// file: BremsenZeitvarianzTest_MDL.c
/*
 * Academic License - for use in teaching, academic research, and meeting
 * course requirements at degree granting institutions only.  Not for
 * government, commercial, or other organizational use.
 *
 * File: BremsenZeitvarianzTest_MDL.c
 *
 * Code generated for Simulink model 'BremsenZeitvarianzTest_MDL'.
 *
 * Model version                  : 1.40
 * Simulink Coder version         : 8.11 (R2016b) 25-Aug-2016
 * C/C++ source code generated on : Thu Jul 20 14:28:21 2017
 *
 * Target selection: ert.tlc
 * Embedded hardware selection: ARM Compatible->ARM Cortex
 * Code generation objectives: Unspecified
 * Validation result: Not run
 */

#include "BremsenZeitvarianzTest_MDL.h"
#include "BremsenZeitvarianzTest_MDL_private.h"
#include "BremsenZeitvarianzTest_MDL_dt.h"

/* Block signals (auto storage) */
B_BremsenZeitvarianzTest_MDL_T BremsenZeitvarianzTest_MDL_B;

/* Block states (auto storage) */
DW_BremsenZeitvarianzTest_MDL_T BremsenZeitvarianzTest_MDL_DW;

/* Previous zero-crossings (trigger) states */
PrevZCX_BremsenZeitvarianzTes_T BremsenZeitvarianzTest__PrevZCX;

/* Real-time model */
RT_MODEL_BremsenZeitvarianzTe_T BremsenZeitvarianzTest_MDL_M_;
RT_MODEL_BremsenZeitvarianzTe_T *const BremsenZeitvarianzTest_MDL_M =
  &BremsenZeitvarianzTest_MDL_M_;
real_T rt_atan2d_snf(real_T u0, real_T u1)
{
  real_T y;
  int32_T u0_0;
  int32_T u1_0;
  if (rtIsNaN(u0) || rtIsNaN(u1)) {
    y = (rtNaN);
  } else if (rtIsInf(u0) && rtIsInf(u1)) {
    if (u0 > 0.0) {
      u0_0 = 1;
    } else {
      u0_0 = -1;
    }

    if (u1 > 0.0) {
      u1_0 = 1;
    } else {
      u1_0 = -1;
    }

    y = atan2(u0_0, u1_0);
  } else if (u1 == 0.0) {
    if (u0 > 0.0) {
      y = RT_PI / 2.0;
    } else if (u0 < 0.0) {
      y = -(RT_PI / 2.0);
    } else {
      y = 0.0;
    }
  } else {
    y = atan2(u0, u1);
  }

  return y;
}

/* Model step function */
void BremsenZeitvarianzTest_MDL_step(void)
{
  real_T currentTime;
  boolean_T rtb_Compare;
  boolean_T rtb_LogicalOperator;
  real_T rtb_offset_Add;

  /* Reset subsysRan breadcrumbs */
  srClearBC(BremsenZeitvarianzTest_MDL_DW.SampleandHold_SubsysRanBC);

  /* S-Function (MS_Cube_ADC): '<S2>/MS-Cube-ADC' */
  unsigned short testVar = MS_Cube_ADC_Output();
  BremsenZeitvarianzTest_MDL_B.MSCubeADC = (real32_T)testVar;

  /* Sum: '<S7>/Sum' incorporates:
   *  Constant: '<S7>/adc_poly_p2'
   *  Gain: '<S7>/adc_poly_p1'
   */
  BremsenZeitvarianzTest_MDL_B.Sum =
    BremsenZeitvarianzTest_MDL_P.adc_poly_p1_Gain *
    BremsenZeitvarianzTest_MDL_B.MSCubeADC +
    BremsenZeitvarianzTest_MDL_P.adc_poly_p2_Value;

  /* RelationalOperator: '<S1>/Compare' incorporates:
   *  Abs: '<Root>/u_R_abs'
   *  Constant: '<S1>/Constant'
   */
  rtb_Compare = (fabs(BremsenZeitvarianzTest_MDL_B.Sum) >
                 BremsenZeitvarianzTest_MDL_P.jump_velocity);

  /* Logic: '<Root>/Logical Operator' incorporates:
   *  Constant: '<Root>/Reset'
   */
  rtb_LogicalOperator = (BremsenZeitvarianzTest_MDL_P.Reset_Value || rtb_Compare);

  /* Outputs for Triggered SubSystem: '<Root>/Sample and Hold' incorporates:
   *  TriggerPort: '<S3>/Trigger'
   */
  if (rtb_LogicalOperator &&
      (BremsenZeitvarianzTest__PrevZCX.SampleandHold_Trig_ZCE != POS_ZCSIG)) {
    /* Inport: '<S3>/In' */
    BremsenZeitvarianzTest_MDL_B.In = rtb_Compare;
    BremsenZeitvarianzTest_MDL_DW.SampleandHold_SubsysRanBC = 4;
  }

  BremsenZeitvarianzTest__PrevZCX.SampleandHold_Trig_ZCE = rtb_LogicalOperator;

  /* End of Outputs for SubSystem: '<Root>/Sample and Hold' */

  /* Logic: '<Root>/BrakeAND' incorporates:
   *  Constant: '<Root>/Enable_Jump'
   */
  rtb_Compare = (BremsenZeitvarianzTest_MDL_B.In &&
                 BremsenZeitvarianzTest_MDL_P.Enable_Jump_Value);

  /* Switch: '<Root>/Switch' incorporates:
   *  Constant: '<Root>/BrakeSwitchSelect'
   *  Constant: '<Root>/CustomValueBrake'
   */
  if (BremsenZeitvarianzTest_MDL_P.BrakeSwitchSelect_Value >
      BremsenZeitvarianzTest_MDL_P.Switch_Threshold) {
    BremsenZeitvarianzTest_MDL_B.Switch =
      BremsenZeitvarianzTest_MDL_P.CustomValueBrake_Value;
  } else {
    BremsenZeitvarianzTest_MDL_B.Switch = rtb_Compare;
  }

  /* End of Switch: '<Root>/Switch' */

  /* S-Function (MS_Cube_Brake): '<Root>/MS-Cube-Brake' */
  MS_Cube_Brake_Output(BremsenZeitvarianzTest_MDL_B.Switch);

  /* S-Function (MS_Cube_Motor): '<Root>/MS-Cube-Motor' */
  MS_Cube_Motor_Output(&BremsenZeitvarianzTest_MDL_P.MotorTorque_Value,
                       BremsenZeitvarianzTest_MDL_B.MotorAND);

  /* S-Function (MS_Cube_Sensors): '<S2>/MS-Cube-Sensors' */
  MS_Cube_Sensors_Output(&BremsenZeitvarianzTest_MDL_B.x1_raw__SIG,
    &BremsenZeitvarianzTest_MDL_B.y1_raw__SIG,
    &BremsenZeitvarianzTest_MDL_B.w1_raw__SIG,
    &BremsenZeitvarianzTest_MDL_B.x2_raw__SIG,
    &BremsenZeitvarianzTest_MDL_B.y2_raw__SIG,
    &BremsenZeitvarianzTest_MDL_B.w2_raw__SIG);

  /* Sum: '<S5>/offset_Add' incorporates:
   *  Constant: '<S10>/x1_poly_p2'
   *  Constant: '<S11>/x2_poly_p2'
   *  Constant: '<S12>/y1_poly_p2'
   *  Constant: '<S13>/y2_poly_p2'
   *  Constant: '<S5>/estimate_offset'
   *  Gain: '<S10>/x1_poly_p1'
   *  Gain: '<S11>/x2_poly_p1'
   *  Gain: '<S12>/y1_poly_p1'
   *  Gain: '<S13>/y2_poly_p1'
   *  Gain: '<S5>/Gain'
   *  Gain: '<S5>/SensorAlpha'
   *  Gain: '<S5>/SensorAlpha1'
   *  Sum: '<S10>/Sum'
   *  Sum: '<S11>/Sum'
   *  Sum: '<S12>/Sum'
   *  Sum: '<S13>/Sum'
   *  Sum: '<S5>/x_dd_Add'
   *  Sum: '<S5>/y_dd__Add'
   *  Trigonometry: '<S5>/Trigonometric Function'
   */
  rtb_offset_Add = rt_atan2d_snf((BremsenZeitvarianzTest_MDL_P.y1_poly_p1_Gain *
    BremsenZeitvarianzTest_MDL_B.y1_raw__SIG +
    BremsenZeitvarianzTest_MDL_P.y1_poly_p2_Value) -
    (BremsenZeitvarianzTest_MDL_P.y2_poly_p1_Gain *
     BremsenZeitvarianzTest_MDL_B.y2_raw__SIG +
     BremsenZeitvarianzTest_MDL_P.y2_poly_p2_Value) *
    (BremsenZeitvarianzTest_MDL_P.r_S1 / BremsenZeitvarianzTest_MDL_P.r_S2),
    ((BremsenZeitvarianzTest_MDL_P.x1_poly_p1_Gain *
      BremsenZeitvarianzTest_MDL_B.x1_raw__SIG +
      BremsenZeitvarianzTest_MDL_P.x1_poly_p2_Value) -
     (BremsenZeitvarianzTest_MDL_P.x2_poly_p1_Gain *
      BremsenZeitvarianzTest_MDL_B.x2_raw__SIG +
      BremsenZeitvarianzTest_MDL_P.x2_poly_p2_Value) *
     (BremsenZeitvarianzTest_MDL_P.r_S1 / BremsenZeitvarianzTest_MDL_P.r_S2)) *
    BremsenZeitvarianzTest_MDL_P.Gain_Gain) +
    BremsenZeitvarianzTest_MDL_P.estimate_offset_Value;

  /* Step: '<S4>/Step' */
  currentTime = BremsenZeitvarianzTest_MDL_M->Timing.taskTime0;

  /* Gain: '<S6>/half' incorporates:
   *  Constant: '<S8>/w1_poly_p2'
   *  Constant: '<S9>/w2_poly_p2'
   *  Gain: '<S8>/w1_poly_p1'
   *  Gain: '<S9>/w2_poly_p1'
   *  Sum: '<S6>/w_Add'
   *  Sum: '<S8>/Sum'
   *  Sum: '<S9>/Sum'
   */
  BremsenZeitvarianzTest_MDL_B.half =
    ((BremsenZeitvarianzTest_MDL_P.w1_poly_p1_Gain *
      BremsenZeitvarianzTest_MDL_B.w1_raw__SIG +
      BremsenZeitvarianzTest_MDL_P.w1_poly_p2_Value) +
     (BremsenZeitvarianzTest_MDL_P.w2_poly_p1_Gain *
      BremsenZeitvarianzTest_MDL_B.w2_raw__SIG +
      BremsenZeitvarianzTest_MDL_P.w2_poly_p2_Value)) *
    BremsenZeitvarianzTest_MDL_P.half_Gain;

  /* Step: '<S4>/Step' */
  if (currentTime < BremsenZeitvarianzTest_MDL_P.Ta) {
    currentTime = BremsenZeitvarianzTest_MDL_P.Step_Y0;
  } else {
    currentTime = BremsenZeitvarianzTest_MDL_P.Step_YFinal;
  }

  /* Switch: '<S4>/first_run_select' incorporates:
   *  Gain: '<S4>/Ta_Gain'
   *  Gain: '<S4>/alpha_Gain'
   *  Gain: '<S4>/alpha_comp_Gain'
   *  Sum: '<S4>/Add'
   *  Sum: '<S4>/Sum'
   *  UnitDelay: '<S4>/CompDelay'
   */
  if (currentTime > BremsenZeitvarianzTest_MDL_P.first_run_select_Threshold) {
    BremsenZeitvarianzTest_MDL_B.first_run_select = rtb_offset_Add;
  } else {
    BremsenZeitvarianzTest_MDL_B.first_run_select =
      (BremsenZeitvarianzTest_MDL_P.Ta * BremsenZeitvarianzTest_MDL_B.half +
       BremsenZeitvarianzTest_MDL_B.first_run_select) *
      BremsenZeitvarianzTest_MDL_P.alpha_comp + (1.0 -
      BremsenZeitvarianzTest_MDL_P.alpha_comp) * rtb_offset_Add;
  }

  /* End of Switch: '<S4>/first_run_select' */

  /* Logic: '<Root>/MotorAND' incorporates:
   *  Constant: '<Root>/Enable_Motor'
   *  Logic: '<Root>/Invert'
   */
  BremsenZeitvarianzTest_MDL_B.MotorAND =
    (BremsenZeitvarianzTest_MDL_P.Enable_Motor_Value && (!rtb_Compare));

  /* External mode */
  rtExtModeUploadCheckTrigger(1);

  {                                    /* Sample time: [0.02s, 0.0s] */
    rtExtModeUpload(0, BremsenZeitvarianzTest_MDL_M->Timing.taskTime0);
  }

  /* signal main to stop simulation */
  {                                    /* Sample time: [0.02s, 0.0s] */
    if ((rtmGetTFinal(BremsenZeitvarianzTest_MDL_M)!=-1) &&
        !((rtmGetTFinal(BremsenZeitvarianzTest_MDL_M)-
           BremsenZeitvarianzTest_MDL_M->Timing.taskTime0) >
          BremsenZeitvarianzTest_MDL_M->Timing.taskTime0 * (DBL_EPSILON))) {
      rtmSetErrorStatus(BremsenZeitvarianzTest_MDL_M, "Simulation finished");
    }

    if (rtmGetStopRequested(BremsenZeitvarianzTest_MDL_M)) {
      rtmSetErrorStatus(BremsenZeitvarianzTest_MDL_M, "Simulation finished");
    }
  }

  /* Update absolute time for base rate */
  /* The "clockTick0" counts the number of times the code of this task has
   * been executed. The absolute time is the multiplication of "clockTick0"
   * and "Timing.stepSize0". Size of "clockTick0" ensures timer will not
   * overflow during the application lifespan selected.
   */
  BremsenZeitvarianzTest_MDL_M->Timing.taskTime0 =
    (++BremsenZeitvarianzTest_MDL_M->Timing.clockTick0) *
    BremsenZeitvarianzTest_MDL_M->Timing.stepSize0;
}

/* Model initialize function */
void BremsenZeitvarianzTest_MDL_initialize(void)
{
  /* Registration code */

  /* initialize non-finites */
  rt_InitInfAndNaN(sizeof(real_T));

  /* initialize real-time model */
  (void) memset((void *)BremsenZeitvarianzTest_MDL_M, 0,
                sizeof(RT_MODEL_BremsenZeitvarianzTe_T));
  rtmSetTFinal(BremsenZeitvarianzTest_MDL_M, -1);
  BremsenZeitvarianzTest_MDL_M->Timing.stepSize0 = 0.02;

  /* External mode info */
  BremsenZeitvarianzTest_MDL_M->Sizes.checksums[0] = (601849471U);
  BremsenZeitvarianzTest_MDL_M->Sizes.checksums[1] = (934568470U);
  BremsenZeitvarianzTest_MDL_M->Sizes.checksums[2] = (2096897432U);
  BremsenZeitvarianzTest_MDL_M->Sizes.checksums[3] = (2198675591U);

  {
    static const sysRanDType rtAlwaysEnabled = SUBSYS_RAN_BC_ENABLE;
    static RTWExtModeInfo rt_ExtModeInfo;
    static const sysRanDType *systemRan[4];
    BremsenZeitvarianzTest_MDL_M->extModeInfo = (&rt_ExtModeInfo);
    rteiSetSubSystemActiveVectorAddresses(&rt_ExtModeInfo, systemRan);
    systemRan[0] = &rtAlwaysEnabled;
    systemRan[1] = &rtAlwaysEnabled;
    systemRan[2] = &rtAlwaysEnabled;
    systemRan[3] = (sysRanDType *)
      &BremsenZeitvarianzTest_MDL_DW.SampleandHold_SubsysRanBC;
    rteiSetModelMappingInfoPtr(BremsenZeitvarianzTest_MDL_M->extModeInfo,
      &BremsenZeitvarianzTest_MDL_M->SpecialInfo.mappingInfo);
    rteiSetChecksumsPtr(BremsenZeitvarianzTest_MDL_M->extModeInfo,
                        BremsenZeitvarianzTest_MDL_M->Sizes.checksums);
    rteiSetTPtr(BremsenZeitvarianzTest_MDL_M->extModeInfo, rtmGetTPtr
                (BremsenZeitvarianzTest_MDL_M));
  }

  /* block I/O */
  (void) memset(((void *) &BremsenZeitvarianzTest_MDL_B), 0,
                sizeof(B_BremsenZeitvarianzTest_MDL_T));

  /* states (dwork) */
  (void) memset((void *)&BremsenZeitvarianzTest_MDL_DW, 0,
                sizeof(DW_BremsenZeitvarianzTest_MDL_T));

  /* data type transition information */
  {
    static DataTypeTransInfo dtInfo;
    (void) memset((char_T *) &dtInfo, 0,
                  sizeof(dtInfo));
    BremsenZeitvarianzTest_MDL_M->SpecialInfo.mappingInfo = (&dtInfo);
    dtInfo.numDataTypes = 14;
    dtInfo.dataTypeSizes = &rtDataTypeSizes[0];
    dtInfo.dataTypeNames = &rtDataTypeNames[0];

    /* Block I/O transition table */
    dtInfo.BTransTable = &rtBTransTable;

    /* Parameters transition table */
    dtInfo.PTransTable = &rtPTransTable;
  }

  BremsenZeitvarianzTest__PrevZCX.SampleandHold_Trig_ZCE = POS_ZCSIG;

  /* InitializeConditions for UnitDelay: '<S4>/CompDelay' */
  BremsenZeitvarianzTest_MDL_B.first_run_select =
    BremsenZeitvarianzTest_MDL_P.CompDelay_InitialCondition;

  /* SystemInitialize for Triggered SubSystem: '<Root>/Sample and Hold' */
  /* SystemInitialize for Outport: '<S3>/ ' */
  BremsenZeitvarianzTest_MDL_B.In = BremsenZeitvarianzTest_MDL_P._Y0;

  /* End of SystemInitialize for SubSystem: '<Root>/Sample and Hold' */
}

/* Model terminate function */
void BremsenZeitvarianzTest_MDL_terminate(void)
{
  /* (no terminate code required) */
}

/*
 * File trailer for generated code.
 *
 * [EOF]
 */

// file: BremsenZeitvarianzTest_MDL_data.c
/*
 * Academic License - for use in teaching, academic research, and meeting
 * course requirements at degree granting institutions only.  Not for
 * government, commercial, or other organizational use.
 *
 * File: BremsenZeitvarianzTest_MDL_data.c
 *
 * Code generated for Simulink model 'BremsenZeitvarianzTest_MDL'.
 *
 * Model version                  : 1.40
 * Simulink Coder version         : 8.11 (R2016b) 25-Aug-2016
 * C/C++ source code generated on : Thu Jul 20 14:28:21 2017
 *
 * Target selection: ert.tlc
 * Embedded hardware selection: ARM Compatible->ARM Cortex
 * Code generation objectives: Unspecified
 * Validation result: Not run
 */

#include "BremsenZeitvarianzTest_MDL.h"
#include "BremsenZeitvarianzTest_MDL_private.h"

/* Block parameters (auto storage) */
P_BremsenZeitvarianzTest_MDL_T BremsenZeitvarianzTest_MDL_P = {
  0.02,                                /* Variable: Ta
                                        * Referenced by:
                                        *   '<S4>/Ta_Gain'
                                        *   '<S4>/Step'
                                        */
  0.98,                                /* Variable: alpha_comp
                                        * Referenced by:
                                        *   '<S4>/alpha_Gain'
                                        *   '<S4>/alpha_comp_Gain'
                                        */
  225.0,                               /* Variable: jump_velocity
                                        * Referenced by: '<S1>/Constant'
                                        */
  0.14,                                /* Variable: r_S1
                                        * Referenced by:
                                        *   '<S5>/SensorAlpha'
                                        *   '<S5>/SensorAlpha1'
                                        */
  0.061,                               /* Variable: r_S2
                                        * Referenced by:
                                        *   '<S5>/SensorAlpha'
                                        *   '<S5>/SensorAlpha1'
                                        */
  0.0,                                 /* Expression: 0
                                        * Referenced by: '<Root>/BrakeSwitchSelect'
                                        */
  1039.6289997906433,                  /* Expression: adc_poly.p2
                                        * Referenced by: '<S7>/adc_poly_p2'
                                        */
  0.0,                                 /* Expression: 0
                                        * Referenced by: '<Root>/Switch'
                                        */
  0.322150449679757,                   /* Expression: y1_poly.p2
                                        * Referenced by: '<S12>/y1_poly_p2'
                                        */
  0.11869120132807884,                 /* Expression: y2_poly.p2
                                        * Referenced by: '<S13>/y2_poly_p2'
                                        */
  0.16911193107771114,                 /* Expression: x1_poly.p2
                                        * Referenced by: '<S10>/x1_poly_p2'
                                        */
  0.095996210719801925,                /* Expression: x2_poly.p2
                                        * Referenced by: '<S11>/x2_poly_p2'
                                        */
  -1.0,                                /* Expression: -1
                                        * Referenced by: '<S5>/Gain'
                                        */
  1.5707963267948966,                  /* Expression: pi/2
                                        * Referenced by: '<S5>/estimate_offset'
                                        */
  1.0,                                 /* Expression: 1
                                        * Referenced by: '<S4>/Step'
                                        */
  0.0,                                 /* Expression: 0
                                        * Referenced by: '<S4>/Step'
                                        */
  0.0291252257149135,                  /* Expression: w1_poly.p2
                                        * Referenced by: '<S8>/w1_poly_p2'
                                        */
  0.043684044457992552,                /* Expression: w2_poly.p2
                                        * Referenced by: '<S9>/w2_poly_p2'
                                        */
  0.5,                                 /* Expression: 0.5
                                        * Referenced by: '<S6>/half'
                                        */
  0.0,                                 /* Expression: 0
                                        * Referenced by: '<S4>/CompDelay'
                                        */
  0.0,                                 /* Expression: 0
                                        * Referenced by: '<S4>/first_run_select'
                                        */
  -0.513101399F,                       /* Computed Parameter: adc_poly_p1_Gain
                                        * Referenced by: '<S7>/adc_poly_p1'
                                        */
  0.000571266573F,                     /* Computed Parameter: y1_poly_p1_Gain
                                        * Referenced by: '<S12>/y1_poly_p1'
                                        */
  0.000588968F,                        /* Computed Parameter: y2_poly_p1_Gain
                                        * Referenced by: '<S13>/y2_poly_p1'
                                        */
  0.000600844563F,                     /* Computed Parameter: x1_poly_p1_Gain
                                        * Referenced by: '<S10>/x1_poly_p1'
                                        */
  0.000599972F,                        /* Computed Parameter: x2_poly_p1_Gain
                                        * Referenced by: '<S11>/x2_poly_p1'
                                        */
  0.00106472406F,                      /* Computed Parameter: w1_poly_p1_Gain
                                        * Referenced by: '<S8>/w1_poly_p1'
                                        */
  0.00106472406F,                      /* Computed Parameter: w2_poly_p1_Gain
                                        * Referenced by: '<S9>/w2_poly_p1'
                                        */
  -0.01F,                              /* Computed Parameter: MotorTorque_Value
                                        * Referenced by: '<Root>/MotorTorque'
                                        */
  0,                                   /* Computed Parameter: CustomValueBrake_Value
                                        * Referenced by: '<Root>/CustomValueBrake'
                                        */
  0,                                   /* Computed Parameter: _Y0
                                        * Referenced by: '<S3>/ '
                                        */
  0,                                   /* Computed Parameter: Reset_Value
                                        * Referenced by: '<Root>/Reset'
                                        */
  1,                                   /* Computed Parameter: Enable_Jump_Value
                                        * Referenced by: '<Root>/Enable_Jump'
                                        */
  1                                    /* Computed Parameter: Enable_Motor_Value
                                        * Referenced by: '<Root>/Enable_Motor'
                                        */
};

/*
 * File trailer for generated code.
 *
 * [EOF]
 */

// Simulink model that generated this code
simulink model "BremsenZeitvarianzTest_MDL"  (R2016b)
settings: Solver=FixedStepAuto  StartTime=0.0  StopTime=inf  FixedStep=Ta  RelTol=1e-3
values from neighbouring files (symbols this model uses):
  alpha_comp = 0.98    [ModelSetup.m]
  jump_velocity = 200    [ModelSetup.m]
  r_S1 = 0.14    [ModelSetup.m]
  r_S2 = 0.061    [ModelSetup.m]
  Ta = 0.02    [ModelSetup.m]
undefined symbols (not defined in the file or in its folder): adc_poly, w1_poly, w2_poly, x1_poly, x2_poly, y1_poly, y2_poly
libraries: MSCubeLibrary x4, simulink x1, dspsigops x1

== system BremsenZeitvarianzTest_MDL ==
  BrakeAND : Logic  AllPortsSameDT=off  OutDataTypeStr=boolean
  BrakeFlag : Scope
  BrakeSwitchSelect : Constant  Value=0
  Compare To Constant : simulink/Logic and Bit Operations/Compare To Constant  relop=>  const=jump_velocity  OutDataTypeStr=boolean
  CustomValueBrake : Constant  Value=0  OutDataTypeStr=boolean
  DebugScope : Scope
  Enable_Jump : Constant  OutDataTypeStr=boolean
  Enable_Motor : Constant  OutDataTypeStr=boolean
  Invert : Logic  Operator=NOT  AllPortsSameDT=off  OutDataTypeStr=boolean
  Logical Operator : Logic  Operator=OR  AllPortsSameDT=off  OutDataTypeStr=boolean
  MS-Cube-Brake : MSCubeLibrary/MS-Cube-Brake
  MS-Cube-Motor : MSCubeLibrary/MS-Cube-Motor
  Measurement : Subsystem
  MotorAND : Logic  AllPortsSameDT=off  OutDataTypeStr=boolean
  MotorTorque : Constant  Value=-0.01  OutDataTypeStr=single
  Reset : Constant  Value=0  OutDataTypeStr=boolean
  Sample and Hold : dspsigops/Sample and Hold  trig=Rising edge  initCond=0  latchinput=off
  Switch : Switch  Criteria=u2 > Threshold
  phi_Scope : Scope
  u_K_Scope : Scope
  u_R_Scope : Scope
  u_R_abs : Abs
  wires:
  Measurement/1(phi__OUT) -> phi_Scope/1  "phi__SIG"
  Measurement/2(u_K__OUT) -> u_K_Scope/1  "u_K__SIG"
  Measurement/3(u_R__OUT) -> u_R_abs/1, u_R_Scope/1  "u_R__SIG"
  u_R_abs/1 -> Compare To Constant/1
  Compare To Constant/1 -> Logical Operator/2, Sample and Hold/1
  Enable_Jump/1 -> BrakeAND/2
  BrakeAND/1 -> Switch/3, Invert/1
  Enable_Motor/1 -> MotorAND/1
  Invert/1 -> MotorAND/2
  MotorAND/1 -> MS-Cube-Motor/2
  MotorTorque/1 -> MS-Cube-Motor/1
  Sample and Hold/1 -> DebugScope/1, BrakeAND/1
  Logical Operator/1 -> Sample and Hold/Trigger
  Reset/1 -> Logical Operator/1
  BrakeSwitchSelect/1 -> Switch/2
  CustomValueBrake/1 -> Switch/1
  Switch/1 -> BrakeFlag/1, MS-Cube-Brake/1

== system BremsenZeitvarianzTest_MDL/Measurement ==
  ComplementaryFilter : Subsystem
  MS-Cube-ADC : MSCubeLibrary/MS-Cube-ADC
  MS-Cube-Sensors : MSCubeLibrary/MS-Cube-Sensors
  PhiEstimate : Subsystem
  WAverage : Subsystem
  adc_Calibration : Subsystem
  w1_Calibration : Subsystem
  w2_Calibration : Subsystem
  x1_Calibration : Subsystem
  x2_Calibration : Subsystem
  y1_Calibration : Subsystem
  y2_Calibration : Subsystem
  phi__OUT : Outport
  u_K__OUT : Outport  Port=2
  u_R__OUT : Outport  Port=3
  wires:
  MS-Cube-Sensors/5 -> y2_Calibration/1(y2_raw__IN)  "y2_raw__SIG"
  MS-Cube-Sensors/6 -> w2_Calibration/1(w2_raw__IN)  "w2_raw__SIG"
  x1_Calibration/1(x1__OUT) -> PhiEstimate/1(x1_dd__IN)
  y1_Calibration/1(y1__OUT) -> PhiEstimate/2(y1_d__IN)
  x2_Calibration/1(x2__OUT) -> PhiEstimate/3(x2_dd__IN)
  y2_Calibration/1(y2__OUT) -> PhiEstimate/4(y2_dd__IN)
  MS-Cube-Sensors/2 -> y1_Calibration/1(y1_raw__IN)  "y1_raw__SIG"
  MS-Cube-Sensors/3 -> w1_Calibration/1(w1_raw__IN)  "w1_raw__SIG"
  MS-Cube-Sensors/1 -> x1_Calibration/1(x1_raw__IN)  "x1_raw__SIG"
  MS-Cube-Sensors/4 -> x2_Calibration/1(x2_raw__IN)  "x2_raw__SIG"
  ComplementaryFilter/1(phi_C__OUT) -> phi__OUT/1  "phi_C__SIG"
  adc_Calibration/1(w_R__OUT) -> u_R__OUT/1
  w2_Calibration/1(w2__OUT) -> WAverage/2(w2__IN)
  w1_Calibration/1(w1__OUT) -> WAverage/1(w1__IN)
  WAverage/1(w__OUT) -> u_K__OUT/1, ComplementaryFilter/2(w__IN)  "w__SIG"
  MS-Cube-ADC/1 -> adc_Calibration/1(adc_raw__IN)
  PhiEstimate/1(phi_A__OUT) -> ComplementaryFilter/1(phi_A__IN)  "phi_A__SIG"

== system BremsenZeitvarianzTest_MDL/Measurement/ComplementaryFilter ==
  phi_A__IN : Inport
  w__IN : Inport  Port=2
  Add : Sum
  CompDelay : UnitDelay  SampleTime=Ta
  Step : Step  Time=Ta  Before=1  After=0  SampleTime=Ta
  Sum : Sum  Inputs=|++
  Ta_Gain : Gain  Gain=Ta
  alpha_Gain : Gain  Gain=alpha_comp
  alpha_comp_Gain : Gain  Gain=1-alpha_comp
  first_run_select : Switch  Criteria=u2 > Threshold
  phi_C__OUT : Outport
  wires:
  w__IN/1 -> Ta_Gain/1
  Ta_Gain/1 -> Sum/1
  Sum/1 -> alpha_Gain/1
  phi_A__IN/1 -> first_run_select/1, alpha_comp_Gain/1
  alpha_comp_Gain/1 -> Add/1
  alpha_Gain/1 -> Add/2
  Add/1 -> first_run_select/3
  first_run_select/1 -> CompDelay/1, phi_C__OUT/1
  CompDelay/1 -> Sum/2
  Step/1 -> first_run_select/2

== system BremsenZeitvarianzTest_MDL/Measurement/PhiEstimate ==
  x1_dd__IN : Inport
  y1_d__IN : Inport  Port=2
  x2_dd__IN : Inport  Port=3
  y2_dd__IN : Inport  Port=4
  Gain : Gain  Gain=-1
  SensorAlpha : Gain  Gain=r_S1/r_S2
  SensorAlpha1 : Gain  Gain=r_S1/r_S2
  Trigonometric Function : Trigonometry  Operator=atan2
  estimate_offset : Constant  Value=pi/2
  offset_Add : Sum
  x_dd_Add : Sum  Inputs=+-
  y_dd__Add : Sum  Inputs=+-
  phi_A__OUT : Outport
  wires:
  x2_dd__IN/1 -> SensorAlpha/1
  y2_dd__IN/1 -> SensorAlpha1/1
  x1_dd__IN/1 -> x_dd_Add/1
  SensorAlpha/1 -> x_dd_Add/2
  y1_d__IN/1 -> y_dd__Add/1
  SensorAlpha1/1 -> y_dd__Add/2
  x_dd_Add/1 -> Gain/1
  y_dd__Add/1 -> Trigonometric Function/1
  Gain/1 -> Trigonometric Function/2
  Trigonometric Function/1 -> offset_Add/1
  estimate_offset/1 -> offset_Add/2
  offset_Add/1 -> phi_A__OUT/1

== system BremsenZeitvarianzTest_MDL/Measurement/WAverage ==
  w1__IN : Inport
  w2__IN : Inport  Port=2
  half : Gain  Gain=0.5
  w_Add : Sum
  w__OUT : Outport
  wires:
  w2__IN/1 -> w_Add/2
  w1__IN/1 -> w_Add/1
  w_Add/1 -> half/1
  half/1 -> w__OUT/1

== system BremsenZeitvarianzTest_MDL/Measurement/adc_Calibration ==
  adc_raw__IN : Inport
  Sum : Sum  Inputs=|++
  adc_poly_p1 : Gain  Gain=adc_poly.p1
  adc_poly_p2 : Constant  Value=adc_poly.p2
  w_R__OUT : Outport
  wires:
  Sum/1 -> w_R__OUT/1
  adc_poly_p2/1 -> Sum/2
  adc_poly_p1/1 -> Sum/1
  adc_raw__IN/1 -> adc_poly_p1/1

== system BremsenZeitvarianzTest_MDL/Measurement/w1_Calibration ==
  w1_raw__IN : Inport
  Sum : Sum  Inputs=|++
  w1_poly_p1 : Gain  Gain=w1_poly.p1
  w1_poly_p2 : Constant  Value=w1_poly.p2
  w1__OUT : Outport
  wires:
  Sum/1 -> w1__OUT/1
  w1_poly_p2/1 -> Sum/2
  w1_poly_p1/1 -> Sum/1
  w1_raw__IN/1 -> w1_poly_p1/1

== system BremsenZeitvarianzTest_MDL/Measurement/w2_Calibration ==
  w2_raw__IN : Inport
  Sum : Sum  Inputs=|++
  w2_poly_p1 : Gain  Gain=w2_poly.p1
  w2_poly_p2 : Constant  Value=w2_poly.p2
  w2__OUT : Outport
  wires:
  w2_raw__IN/1 -> w2_poly_p1/1
  w2_poly_p1/1 -> Sum/1
  w2_poly_p2/1 -> Sum/2
  Sum/1 -> w2__OUT/1

== system BremsenZeitvarianzTest_MDL/Measurement/x1_Calibration ==
  x1_raw__IN : Inport
  Sum : Sum  Inputs=|++
  x1_poly_p1 : Gain  Gain=x1_poly.p1
  x1_poly_p2 : Constant  Value=x1_poly.p2
  x1__OUT : Outport
  wires:
  Sum/1 -> x1__OUT/1
  x1_poly_p2/1 -> Sum/2
  x1_poly_p1/1 -> Sum/1
  x1_raw__IN/1 -> x1_poly_p1/1

== system BremsenZeitvarianzTest_MDL/Measurement/x2_Calibration ==
  x2_raw__IN : Inport
  Sum : Sum  Inputs=|++
  x2_poly_p1 : Gain  Gain=x2_poly.p1
  x2_poly_p2 : Constant  Value=x2_poly.p2
  x2__OUT : Outport
  wires:
  x2_raw__IN/1 -> x2_poly_p1/1
  x2_poly_p1/1 -> Sum/1
  x2_poly_p2/1 -> Sum/2
  Sum/1 -> x2__OUT/1

== system BremsenZeitvarianzTest_MDL/Measurement/y1_Calibration ==
  y1_raw__IN : Inport
  Sum : Sum  Inputs=|++
  y1_poly_p1 : Gain  Gain=y1_poly.p1
  y1_poly_p2 : Constant  Value=y1_poly.p2
  y1__OUT : Outport
  wires:
  y1_raw__IN/1 -> y1_poly_p1/1
  y1_poly_p1/1 -> Sum/1
  y1_poly_p2/1 -> Sum/2
  Sum/1 -> y1__OUT/1

== system BremsenZeitvarianzTest_MDL/Measurement/y2_Calibration ==
  y2_raw__IN : Inport
  Sum : Sum  Inputs=|++
  y2_poly_p1 : Gain  Gain=y2_poly.p1
  y2_poly_p2 : Constant  Value=y2_poly.p2
  y2__OUT : Outport
  wires:
  Sum/1 -> y2__OUT/1
  y2_poly_p2/1 -> Sum/2
  y2_poly_p1/1 -> Sum/1
  y2_raw__IN/1 -> y2_poly_p1/1
